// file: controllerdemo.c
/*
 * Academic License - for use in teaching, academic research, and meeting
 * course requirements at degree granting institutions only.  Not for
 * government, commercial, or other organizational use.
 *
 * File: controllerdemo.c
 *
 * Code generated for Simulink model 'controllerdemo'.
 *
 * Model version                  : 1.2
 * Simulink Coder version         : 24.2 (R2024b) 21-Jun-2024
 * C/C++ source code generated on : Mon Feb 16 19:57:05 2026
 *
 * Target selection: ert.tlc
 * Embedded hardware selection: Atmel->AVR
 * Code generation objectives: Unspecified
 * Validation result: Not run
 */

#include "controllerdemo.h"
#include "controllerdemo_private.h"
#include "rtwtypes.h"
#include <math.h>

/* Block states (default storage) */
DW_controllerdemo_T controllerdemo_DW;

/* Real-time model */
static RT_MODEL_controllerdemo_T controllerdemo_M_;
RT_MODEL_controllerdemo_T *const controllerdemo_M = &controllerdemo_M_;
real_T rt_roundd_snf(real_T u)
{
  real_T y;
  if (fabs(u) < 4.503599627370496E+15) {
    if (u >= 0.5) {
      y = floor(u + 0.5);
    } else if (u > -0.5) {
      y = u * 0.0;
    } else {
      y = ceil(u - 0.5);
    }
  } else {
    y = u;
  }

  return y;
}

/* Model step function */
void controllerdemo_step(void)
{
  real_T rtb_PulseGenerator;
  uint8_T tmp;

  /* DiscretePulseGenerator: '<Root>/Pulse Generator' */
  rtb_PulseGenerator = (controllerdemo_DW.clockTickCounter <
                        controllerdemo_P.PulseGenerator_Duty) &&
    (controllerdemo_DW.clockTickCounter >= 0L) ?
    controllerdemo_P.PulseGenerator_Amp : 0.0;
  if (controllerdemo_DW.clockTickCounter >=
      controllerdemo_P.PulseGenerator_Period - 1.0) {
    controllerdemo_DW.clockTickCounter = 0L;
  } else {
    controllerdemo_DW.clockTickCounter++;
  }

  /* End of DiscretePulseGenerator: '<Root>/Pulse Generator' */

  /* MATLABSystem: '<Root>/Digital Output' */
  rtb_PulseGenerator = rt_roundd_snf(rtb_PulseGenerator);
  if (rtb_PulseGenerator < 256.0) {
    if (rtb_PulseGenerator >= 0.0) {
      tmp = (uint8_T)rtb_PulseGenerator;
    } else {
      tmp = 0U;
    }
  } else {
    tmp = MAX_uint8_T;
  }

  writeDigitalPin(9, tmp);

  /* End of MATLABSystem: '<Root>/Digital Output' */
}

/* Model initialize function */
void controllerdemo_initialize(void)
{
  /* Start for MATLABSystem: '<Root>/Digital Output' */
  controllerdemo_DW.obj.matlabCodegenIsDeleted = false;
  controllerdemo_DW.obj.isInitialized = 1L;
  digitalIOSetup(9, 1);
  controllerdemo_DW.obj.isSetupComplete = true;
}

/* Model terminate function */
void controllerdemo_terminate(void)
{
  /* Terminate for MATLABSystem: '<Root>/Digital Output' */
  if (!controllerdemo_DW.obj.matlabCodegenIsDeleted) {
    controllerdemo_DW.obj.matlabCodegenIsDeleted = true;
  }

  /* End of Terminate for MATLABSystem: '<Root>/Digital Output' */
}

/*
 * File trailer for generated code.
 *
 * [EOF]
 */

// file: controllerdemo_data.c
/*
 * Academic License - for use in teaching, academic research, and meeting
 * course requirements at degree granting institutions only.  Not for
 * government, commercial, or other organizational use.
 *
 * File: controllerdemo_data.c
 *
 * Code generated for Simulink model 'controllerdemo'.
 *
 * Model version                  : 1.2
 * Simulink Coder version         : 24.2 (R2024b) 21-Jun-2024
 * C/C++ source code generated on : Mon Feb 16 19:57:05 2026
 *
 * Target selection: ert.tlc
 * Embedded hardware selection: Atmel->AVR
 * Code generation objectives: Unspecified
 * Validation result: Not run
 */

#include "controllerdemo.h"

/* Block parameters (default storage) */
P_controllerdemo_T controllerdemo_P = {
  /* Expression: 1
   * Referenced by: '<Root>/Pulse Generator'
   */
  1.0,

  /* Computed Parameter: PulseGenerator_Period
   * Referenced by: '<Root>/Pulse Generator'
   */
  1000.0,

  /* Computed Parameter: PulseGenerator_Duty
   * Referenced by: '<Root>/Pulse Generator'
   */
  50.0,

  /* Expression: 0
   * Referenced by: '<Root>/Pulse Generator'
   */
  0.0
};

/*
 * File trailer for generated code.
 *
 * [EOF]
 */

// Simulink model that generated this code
simulink model "controllerdemo"  (R2024b)
settings: Solver=FixedStepAuto  StartTime=0.0  StopTime=inf  FixedStep=0.01  RelTol=1e-3  EnableMultiTasking=on
libraries: arduinolib x1

== system controllerdemo ==
  Digital Output : arduinolib/Digital Output  pinNumber=9  Direction=output  blockPlatform=arduino
  Pulse Generator : DiscretePulseGenerator  PulseType=Time based  Period=10  PulseWidth=5
  wires:
  Pulse Generator/1 -> Digital Output/1
